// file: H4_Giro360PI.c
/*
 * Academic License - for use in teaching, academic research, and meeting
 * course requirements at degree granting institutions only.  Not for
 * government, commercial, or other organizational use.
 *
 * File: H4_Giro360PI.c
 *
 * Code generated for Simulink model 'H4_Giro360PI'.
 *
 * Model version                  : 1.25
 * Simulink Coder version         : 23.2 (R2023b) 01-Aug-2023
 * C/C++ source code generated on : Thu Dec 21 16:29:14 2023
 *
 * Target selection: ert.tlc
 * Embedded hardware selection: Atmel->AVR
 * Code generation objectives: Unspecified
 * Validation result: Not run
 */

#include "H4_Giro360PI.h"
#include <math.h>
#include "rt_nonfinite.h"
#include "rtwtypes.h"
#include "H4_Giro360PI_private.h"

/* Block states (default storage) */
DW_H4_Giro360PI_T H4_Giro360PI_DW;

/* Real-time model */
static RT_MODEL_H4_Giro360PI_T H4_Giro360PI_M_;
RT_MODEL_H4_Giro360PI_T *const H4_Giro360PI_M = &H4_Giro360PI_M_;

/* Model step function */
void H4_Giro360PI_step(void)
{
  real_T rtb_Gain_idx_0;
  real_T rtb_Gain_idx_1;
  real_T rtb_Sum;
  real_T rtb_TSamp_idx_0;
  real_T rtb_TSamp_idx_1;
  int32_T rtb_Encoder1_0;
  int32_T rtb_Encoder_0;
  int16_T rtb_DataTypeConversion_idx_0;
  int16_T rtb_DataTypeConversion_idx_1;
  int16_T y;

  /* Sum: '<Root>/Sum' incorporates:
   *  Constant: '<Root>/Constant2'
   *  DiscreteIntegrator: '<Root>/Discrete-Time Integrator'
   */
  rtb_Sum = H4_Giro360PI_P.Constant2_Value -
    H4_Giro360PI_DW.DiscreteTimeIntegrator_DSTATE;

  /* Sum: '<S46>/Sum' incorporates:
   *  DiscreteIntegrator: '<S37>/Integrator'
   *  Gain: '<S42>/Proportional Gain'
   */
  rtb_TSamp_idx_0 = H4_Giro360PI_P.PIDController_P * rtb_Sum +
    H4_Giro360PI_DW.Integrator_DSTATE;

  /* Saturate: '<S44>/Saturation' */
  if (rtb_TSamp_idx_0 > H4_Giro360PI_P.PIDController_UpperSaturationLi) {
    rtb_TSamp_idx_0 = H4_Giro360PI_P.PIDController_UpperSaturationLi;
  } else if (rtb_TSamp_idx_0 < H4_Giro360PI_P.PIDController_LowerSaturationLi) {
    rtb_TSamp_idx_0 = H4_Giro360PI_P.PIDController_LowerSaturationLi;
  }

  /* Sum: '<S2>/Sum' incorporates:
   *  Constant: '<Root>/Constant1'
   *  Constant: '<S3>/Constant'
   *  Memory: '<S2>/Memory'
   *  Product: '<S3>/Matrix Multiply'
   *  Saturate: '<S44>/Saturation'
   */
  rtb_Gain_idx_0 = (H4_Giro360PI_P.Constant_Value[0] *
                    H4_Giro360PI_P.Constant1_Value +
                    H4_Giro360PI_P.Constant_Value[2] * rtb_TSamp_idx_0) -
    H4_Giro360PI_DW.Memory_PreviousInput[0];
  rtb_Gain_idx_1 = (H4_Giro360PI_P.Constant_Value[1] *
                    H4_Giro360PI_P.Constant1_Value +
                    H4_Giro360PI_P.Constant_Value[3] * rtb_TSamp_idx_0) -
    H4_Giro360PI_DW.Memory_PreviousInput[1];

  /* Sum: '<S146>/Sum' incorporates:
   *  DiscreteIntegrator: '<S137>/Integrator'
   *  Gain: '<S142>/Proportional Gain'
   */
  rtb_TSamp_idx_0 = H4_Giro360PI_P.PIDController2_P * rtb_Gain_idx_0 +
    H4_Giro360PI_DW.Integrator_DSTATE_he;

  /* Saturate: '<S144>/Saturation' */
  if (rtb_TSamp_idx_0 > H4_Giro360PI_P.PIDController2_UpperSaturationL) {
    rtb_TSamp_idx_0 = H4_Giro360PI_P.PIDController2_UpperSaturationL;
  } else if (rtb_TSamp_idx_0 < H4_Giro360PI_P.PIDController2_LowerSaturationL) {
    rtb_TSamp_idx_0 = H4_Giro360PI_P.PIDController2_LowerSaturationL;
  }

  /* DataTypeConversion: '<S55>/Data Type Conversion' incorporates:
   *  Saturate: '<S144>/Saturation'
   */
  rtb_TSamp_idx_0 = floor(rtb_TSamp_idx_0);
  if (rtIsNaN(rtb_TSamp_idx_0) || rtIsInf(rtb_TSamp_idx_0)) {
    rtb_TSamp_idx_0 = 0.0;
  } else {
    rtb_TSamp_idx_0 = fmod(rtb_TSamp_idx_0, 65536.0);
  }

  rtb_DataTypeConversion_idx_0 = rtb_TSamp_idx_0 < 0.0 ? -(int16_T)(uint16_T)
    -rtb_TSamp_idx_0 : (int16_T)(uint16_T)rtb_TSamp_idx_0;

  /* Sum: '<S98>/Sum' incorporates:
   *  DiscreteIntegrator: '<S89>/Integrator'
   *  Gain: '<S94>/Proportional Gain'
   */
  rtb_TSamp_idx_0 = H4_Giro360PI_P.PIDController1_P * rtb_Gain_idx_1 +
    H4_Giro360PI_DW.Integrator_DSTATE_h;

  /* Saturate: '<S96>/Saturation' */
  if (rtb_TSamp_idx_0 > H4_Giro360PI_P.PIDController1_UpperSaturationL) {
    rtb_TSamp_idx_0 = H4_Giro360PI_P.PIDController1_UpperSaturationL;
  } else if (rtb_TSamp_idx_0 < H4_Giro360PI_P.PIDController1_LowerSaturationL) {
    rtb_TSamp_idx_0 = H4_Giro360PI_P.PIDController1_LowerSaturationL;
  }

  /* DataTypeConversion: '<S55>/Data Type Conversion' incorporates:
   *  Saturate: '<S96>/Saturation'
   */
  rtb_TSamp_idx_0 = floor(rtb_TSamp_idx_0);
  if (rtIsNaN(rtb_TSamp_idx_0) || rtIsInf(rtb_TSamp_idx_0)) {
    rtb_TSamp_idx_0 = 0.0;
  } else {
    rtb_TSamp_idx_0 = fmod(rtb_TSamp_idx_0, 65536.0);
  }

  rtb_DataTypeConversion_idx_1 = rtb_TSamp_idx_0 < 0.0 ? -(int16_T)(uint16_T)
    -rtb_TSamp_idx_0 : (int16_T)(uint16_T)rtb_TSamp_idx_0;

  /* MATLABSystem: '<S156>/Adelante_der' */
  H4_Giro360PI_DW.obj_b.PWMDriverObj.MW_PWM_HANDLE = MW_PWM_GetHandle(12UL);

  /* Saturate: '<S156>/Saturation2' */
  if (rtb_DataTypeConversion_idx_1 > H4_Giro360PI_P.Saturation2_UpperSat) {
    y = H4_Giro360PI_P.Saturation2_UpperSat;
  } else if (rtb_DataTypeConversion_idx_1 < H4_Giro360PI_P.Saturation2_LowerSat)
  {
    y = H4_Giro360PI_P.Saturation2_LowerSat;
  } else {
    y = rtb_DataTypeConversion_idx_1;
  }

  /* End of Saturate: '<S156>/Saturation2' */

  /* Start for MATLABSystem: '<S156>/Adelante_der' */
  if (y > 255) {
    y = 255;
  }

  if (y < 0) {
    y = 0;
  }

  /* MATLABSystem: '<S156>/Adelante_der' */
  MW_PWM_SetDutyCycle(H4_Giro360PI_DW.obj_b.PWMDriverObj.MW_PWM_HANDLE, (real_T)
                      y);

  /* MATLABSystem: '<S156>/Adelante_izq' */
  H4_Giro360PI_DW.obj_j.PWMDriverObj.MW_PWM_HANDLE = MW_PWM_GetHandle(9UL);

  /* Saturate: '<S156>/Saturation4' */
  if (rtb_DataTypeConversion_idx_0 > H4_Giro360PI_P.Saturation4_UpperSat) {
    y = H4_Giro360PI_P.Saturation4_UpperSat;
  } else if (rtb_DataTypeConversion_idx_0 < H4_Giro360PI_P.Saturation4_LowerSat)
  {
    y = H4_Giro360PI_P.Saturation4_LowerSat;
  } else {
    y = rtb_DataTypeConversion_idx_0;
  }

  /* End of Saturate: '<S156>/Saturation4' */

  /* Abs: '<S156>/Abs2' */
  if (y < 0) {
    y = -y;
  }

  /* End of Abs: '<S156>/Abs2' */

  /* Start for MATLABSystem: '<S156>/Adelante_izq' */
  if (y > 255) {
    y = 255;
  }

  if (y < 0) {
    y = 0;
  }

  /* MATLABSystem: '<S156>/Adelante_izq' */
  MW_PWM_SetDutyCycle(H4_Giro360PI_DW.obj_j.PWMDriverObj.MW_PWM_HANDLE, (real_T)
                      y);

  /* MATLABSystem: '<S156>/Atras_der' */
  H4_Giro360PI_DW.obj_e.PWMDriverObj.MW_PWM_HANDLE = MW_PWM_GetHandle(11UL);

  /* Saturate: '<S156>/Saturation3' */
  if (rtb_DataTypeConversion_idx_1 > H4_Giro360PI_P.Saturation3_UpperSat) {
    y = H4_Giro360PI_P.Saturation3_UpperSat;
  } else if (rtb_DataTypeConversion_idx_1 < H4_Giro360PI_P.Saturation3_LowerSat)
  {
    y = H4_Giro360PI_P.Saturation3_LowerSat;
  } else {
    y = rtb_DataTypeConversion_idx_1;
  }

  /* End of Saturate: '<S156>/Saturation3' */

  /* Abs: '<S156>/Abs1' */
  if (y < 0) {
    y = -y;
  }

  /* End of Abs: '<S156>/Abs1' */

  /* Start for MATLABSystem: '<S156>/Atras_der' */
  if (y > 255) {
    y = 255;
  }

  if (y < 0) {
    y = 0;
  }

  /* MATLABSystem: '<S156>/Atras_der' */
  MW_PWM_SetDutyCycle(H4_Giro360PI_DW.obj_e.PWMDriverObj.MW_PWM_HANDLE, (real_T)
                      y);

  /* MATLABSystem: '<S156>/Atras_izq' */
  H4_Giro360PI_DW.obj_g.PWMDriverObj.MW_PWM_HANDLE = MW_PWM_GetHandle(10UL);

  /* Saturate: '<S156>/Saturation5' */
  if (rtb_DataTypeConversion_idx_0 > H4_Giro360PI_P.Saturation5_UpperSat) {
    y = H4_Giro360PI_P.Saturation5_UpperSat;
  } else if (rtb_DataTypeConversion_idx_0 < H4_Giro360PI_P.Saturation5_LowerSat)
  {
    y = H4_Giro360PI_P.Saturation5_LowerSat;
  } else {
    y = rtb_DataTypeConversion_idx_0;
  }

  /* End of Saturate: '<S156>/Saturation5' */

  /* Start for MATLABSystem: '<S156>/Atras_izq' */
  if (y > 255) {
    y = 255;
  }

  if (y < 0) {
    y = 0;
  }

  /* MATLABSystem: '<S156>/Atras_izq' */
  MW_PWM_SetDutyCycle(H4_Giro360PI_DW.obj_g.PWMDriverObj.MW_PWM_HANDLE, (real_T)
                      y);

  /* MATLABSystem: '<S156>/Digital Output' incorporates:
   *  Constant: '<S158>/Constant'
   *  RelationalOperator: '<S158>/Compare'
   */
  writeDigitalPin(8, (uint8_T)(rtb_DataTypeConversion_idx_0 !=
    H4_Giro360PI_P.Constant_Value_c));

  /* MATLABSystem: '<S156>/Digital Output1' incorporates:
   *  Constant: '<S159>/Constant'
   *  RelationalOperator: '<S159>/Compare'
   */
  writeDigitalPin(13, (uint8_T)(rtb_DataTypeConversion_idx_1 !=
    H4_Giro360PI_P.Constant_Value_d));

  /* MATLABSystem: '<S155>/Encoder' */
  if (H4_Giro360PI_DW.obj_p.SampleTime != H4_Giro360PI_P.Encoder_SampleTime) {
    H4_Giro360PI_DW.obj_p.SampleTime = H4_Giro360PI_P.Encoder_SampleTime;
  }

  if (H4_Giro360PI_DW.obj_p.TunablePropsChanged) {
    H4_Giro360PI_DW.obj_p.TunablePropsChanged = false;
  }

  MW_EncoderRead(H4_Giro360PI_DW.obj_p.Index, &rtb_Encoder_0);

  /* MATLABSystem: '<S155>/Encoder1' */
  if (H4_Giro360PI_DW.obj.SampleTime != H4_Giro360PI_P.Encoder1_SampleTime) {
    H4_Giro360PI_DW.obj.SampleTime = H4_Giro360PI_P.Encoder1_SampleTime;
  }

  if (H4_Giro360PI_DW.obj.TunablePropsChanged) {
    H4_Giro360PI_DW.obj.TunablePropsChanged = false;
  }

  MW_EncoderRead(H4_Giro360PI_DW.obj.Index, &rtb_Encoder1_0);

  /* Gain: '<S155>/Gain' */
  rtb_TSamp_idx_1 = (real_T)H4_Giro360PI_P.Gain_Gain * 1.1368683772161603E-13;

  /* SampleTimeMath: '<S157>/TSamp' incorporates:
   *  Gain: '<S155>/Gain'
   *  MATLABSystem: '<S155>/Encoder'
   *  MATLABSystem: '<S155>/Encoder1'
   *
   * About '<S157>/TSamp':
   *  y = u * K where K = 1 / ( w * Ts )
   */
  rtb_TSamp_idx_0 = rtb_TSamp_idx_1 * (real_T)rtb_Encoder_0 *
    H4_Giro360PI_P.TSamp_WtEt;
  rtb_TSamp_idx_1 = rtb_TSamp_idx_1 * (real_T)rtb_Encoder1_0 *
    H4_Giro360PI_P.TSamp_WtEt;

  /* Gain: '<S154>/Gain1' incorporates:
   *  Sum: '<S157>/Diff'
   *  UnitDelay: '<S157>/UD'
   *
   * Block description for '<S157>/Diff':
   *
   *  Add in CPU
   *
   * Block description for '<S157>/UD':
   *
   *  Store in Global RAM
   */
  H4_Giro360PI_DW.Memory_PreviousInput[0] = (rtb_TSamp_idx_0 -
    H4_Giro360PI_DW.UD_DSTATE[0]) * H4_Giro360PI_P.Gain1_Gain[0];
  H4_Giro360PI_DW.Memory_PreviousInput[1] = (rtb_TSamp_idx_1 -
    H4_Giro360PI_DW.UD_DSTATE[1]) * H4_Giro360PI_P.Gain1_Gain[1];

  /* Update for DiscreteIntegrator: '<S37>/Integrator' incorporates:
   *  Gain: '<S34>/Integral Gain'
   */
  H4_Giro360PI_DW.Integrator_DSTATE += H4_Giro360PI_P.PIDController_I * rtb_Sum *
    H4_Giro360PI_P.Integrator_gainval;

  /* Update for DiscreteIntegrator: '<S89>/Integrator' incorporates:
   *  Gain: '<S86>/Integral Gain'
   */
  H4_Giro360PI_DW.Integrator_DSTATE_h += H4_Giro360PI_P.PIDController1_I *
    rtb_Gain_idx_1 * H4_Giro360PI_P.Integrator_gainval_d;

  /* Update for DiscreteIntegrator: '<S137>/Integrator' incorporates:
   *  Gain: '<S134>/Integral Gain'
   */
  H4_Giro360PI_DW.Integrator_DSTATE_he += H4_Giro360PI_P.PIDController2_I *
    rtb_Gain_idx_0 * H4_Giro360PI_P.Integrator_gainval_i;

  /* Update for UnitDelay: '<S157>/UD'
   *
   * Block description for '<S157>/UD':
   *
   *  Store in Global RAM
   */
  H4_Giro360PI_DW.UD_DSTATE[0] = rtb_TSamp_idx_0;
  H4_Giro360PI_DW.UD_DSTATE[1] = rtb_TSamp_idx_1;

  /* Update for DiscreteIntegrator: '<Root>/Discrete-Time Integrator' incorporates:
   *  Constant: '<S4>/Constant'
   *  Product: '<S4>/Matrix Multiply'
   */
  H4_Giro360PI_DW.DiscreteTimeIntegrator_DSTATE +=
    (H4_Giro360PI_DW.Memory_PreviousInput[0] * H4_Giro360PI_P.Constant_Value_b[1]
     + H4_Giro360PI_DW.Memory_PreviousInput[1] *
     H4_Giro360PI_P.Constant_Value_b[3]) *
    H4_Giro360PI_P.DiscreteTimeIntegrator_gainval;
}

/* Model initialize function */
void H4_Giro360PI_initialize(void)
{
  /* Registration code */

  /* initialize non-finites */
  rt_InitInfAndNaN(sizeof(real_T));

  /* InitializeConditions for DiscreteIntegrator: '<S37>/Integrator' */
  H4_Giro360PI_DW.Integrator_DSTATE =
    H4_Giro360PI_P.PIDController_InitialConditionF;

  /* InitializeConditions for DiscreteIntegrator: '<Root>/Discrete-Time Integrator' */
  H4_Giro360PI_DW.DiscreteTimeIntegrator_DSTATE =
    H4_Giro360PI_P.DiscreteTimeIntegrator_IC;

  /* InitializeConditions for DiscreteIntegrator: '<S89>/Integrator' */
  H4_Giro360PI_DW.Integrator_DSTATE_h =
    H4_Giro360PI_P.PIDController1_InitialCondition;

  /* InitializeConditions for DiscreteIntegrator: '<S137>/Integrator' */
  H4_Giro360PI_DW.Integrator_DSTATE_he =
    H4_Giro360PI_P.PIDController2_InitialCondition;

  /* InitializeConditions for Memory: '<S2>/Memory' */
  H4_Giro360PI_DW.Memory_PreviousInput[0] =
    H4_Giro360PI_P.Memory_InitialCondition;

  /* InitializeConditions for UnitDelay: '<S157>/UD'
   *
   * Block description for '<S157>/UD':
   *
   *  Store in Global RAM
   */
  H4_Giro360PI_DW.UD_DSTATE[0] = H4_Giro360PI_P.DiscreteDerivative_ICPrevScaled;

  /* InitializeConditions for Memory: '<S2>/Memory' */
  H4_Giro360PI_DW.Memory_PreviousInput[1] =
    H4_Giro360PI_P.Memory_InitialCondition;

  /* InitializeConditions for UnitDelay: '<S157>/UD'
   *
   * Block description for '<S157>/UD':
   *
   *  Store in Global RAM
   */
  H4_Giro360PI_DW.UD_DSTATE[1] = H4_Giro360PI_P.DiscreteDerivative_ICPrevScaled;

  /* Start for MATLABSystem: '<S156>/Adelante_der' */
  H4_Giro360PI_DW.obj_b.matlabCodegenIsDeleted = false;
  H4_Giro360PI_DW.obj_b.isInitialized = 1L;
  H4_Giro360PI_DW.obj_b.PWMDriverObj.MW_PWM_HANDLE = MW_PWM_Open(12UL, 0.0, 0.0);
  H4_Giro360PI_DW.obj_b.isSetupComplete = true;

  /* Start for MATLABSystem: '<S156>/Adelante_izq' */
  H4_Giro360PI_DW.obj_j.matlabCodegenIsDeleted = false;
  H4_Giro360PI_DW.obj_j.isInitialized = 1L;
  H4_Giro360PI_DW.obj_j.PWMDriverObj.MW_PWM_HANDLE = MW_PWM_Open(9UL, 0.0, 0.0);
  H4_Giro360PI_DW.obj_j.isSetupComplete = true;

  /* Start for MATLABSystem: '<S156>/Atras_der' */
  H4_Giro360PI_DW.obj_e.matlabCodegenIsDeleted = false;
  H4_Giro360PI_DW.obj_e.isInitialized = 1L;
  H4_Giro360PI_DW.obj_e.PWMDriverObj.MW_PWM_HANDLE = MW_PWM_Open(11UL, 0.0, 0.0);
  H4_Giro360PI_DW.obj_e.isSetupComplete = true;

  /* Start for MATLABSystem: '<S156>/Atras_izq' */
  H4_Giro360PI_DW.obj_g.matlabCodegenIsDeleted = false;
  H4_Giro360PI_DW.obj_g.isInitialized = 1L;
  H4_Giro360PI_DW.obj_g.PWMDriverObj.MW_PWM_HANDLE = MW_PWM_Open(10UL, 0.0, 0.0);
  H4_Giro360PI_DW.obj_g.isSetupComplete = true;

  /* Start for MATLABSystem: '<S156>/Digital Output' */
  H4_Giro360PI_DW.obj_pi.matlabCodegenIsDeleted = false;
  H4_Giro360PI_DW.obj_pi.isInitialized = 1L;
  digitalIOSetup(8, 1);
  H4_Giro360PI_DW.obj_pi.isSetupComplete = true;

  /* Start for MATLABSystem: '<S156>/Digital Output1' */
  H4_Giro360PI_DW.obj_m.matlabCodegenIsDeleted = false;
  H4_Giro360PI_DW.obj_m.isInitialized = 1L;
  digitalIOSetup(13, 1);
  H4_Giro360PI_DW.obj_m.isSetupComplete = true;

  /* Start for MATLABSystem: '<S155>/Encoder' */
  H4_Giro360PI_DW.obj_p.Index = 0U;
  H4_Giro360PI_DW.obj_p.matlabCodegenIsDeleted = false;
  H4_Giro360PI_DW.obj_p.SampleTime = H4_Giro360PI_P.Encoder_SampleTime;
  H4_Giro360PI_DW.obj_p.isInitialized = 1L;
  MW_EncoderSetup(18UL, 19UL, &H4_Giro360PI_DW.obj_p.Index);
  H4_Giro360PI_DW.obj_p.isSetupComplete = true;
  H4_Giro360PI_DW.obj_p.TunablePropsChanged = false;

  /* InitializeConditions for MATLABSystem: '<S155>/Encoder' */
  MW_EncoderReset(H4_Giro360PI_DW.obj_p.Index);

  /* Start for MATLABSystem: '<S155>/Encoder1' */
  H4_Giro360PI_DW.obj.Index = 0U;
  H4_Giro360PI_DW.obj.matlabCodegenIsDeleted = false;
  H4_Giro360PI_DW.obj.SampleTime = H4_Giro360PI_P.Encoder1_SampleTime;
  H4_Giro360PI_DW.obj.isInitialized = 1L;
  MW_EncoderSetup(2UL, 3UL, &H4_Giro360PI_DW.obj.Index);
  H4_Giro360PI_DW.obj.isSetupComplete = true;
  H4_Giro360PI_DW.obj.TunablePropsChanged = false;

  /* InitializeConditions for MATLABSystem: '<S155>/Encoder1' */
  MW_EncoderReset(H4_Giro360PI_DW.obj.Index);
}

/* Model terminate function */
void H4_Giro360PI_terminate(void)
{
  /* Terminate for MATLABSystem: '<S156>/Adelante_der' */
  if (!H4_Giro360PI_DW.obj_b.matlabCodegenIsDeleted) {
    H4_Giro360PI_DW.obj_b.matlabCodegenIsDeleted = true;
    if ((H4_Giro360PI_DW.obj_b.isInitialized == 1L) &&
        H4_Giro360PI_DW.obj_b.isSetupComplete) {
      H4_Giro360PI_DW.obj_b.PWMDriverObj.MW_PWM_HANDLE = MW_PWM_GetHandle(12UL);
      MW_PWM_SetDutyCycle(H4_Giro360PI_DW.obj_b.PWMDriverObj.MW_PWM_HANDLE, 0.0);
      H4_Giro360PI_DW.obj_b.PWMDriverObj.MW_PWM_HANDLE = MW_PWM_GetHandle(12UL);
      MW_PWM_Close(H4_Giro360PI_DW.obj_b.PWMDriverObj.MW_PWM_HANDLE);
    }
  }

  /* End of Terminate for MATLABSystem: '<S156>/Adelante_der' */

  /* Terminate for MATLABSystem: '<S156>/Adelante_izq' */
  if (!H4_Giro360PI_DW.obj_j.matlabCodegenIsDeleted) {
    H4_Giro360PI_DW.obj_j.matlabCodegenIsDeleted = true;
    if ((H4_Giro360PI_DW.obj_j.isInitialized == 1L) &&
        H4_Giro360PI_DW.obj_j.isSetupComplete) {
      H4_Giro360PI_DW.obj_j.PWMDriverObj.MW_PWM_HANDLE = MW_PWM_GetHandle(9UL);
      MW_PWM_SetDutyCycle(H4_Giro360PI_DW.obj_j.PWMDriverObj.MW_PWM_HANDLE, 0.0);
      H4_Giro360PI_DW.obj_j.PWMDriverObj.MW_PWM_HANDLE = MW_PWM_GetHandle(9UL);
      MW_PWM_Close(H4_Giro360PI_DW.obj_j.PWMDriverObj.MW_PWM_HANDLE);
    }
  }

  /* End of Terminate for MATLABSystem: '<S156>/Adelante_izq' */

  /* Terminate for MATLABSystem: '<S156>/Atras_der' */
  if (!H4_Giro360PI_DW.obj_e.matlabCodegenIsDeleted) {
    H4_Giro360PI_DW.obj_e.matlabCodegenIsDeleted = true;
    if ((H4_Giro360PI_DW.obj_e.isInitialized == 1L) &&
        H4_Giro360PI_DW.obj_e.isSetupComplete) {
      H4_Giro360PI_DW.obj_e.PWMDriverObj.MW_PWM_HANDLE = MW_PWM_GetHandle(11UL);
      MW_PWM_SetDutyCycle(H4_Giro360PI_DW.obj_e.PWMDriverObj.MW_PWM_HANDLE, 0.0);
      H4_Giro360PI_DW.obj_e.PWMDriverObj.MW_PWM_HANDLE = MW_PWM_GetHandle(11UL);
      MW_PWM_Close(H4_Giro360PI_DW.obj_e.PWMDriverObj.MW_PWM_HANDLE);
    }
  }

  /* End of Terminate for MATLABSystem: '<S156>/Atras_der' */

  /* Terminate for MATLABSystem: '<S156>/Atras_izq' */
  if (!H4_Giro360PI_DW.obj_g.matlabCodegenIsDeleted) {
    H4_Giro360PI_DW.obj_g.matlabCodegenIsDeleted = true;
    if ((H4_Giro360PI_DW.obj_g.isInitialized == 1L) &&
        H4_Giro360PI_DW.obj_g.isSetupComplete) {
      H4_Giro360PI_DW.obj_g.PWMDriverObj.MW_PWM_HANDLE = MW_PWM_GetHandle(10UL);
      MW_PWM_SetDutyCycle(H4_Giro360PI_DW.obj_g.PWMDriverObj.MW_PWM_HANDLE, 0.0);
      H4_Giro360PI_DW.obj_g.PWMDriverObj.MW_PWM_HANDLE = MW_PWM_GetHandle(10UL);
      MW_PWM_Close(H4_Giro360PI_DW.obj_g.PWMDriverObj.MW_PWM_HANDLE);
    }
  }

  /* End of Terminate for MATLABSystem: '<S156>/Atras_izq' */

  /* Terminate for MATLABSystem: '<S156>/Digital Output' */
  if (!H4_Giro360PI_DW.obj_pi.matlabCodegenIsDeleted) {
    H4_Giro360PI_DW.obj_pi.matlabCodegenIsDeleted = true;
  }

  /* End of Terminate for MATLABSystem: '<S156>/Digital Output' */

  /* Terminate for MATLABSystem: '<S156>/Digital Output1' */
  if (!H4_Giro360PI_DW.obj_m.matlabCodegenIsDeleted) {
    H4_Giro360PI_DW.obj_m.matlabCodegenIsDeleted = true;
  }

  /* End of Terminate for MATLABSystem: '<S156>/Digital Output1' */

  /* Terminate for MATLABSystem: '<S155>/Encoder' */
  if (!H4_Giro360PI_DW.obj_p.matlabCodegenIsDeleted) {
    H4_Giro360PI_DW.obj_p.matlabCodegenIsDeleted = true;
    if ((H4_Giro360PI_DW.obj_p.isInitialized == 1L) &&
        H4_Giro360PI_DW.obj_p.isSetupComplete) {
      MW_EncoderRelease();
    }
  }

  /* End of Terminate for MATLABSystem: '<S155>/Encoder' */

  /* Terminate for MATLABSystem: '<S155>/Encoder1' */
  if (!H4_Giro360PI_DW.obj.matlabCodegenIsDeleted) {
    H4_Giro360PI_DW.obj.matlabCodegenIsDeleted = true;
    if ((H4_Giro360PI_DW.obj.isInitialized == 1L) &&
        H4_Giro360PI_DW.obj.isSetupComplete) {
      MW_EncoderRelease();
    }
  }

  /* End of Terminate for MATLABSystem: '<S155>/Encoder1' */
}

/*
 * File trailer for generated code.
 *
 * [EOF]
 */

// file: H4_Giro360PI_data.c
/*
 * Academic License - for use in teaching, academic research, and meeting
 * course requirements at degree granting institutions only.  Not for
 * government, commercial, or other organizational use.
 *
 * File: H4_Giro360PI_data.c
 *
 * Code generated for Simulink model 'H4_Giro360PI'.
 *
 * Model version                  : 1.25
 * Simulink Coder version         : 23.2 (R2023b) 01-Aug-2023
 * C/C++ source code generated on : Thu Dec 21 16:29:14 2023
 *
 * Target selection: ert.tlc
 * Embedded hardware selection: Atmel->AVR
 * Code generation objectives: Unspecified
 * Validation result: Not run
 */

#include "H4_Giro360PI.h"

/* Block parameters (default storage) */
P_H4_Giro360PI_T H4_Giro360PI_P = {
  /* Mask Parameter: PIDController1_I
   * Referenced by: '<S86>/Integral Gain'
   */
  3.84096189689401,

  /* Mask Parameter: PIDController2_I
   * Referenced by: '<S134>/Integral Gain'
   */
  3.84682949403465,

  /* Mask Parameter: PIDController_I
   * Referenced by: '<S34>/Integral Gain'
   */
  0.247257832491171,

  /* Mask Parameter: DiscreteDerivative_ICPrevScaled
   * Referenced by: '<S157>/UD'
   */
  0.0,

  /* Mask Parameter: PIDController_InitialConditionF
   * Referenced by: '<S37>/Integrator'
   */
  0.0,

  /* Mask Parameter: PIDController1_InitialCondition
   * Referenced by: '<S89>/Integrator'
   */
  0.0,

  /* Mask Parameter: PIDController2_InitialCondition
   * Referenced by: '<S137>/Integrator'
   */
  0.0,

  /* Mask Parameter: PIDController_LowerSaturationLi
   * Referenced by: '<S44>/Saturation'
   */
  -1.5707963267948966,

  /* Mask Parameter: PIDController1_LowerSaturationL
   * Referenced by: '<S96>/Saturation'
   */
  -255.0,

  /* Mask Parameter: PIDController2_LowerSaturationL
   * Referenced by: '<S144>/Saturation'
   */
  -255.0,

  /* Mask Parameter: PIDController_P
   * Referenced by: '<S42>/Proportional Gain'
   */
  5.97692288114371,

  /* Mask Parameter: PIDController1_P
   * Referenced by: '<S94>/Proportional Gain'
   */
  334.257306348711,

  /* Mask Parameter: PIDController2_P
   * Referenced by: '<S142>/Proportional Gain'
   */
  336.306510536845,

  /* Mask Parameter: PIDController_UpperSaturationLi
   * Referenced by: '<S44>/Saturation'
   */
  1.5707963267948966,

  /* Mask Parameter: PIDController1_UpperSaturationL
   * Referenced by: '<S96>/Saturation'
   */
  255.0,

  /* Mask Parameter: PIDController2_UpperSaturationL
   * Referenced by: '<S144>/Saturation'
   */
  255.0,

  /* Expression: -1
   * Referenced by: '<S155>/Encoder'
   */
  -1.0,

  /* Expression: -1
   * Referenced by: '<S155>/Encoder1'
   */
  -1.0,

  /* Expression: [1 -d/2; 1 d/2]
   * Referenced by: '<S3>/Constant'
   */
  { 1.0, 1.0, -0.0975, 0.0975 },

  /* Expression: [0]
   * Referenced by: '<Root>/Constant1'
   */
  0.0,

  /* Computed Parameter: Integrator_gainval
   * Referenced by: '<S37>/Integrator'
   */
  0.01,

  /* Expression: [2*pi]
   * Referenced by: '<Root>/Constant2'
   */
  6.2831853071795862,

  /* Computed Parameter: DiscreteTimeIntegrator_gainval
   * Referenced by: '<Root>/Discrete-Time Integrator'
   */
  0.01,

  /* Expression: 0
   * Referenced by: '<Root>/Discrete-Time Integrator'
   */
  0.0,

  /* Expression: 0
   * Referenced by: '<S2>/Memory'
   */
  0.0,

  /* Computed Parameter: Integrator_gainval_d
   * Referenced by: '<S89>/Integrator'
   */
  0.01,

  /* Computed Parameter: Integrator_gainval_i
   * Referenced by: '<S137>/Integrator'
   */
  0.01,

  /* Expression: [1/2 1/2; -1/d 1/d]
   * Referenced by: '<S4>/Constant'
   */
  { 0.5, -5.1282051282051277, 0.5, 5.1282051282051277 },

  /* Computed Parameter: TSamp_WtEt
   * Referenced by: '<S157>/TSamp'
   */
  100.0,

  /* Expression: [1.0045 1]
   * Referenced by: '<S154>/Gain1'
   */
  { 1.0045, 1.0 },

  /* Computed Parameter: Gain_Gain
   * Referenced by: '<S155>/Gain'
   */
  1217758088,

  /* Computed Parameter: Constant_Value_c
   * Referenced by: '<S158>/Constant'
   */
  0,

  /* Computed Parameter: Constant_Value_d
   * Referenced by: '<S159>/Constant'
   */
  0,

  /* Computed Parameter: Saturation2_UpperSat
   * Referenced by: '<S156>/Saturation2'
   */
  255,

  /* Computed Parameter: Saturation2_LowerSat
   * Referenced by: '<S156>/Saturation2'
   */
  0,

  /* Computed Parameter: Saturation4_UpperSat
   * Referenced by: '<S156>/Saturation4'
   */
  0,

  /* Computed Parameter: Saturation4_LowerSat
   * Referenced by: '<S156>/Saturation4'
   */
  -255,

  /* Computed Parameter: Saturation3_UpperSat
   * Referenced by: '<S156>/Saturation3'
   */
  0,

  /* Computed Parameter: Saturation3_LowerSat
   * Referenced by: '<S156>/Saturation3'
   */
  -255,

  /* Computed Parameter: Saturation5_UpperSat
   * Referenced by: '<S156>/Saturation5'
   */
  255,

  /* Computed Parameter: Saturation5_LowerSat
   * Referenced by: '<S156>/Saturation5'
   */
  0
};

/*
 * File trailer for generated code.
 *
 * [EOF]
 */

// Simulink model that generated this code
simulink model "H4_Giro360PI"  (R2023b)
settings: Solver=FixedStepDiscrete  StartTime=0.0  StopTime=10  FixedStep=0.01  RelTol=1e-3  EnableMultiTasking=on
model workspace (MAT data in the model file):
  d = 0.195
undefined symbols (not defined in the file or in its folder): DiscIntNeverNeededParam
libraries: slpidlib x1

== system H4_Giro360PI ==
  Constant1 : Constant  Value=[0]
  Constant2 : Constant  Value=[2*pi]
  Demux : Demux  Outputs=2
  Discrete-Time Integrator : DiscreteIntegrator  SampleTime=-1  ICPrevOutput=DiscIntNeverNeededParam  ICPrevScaledInput=DiscIntNeverNeededParam
  Mux : Mux  Inputs=2
  PID Controller : slpidlib/PID Controller  Controller=PI  Form=Parallel  TimeDomain=Discrete-time  UseExternalTs=off  SampleTime=-1  IntegratorMethod=Forward Euler  FilterMethod=Forward Euler  ControllerParametersSource=internal  P=5.97692288114371  I=0.247257832491171  UseKiTs=off  D=0  N=100  UseFilter=on  TunerSelectOption=Transfer Function Based (PID Tuner App)  InitialConditionSource=internal  InitialConditionForIntegrator=0  InitialConditionForFilter=0  DifferentiatorICPrevScaledInput=0  ExternalReset=none  TrackingMode=off  Kt=1  LimitOutput=on  SatLimitsSource=internal  UpperSaturationLimit=2*pi/4  LowerSaturationLimit=-2*pi/4  LinearizeAsGain=off  AntiWindupMode=none  Kb=1  LimitIntegrator=off  UpperIntegratorSaturationLimit=inf  LowerIntegratorSaturationLimit=-inf  POutMin=[]  POutMax=[]  IOutMin=[]  IOutMax=[]  DOutMin=[]  DOutMax=[]  NOutMin=[]  NOutMax=[]  SumOutMin=[]  SumOutMax=[]  SaturationOutMin=[]  SaturationOutMax=[]  PParamMin=[]  PParamMax=[]  IParamMin=[]  IParamMax=[]  DParamMin=[]  DParamMax=[]  NParamMin=[]  NParamMax=[]  KbParamMin=[]  KbParamMax=[]  KtParamMin=[]  KtParamMax=[]  KbOutMin=[]  KbOutMax=[]  KtOutMin=[]  KtOutMax=[]  IntegratorOutMin=[]  IntegratorOutMax=[]  FilterOutMin=[]  FilterOutMax=[]  SumI1OutMin=[]  SumI1OutMax=[]  SumI2OutMin=[]  SumI2OutMax=[]  SumI3OutMin=[]  SumI3OutMax=[]  SumI4OutMin=[]  SumI4OutMax=[]  SumDOutMin=[]  SumDOutMax=[]  DifferentiatorOutMin=[]  DifferentiatorOutMax=[]  FilterDiffOutCoefMin=[]  FilterDiffOutCoefMax=[]  ReciprocalOutMin=[]  ReciprocalOutMax=[]  SumDenOutMin=[]  SumDenOutMax=[]  SumNumOutMin=[]  SumNumOutMax=[]  DivideOutMin=[]  DivideOutMax=[]  UdiffTsProdOutMin=[]  UdiffTsProdOutMax=[]  NTsProdOutMin=[]  NTsProdOutMax=[]  UintegralTsProdOutMin=[]  UintegralTsProdOutMax=[]  UngainTsProdOutMin=[]  UngainTsProdOutMax=[]  ClampingZeroOutDataTypeStr=Inherit: Inherit via back propagation  ClampingZeroOutMin=[]  ClampingZeroOutMax=[]  FilterDenConstantOutDataTypeStr=Inherit: Inherit via back propagation  FilterDenConstantOutMin=[]  FilterDenConstantOutMax=[]  PCopyOutDataTypeStr=Inherit: Inherit via back propagation  PCopyOutMin=[]  PCopyOutMax=[]  NCopyOutDataTypeStr=Inherit: Inherit via back propagation  NCopyOutMin=[]  NCopyOutMax=[]  IntegratorContinuousStateAttributes=''  IntegratorStateMustResolveToSignalObject=off  IntegratorRTWStateStorageClass=Auto  FilterContinuousStateAttributes=''  FilterStateMustResolveToSignalObject=off  FilterRTWStateStorageClass=Auto  ParallelPVariant=InternalParameters  IdealPVariant=Disabled  IVariant=InternalParameters  DVariant=Disabled  IntegratorVariant=Discrete  SatVariant=Enabled  AWVariant=Passthrough  PCopyVariant=Disabled  TRVariant=Disabled  FdbkBlocksVariant=Forward  IdealPFdbkVariant=Disabled  SatFdbkVariant=Disabled  DerivativeFilterVariant=Disabled  NVariant=Disabled  NCopyVariant=Disabled_SignalSpec  FilterICVariant=Disabled  IntegratorICVariant=InternalICs  ExternalResetVariant=Disabled  TRSumVariant=Passthrough  SumFdbkVariant=Disabled  SumVariant=Sum_PI  TsampFilterVariant=InternalTs  TsampNgainVariant=Passthrough  TsampIntegralVariant=Disabled_SignalSpec  ExternalSaturationOutDataTypeStr=Inherit: Same as second input
  Subsystem Reference : Subsystem  ReferencedSubsystem=Piero_ControladoZ_memoria
  Subsystem Reference1 : Subsystem  ReferencedSubsystem=MCI2
  Subsystem Reference2 : Subsystem  ReferencedSubsystem=MCD2
  Subsystem Reference4 : Subsystem  ReferencedSubsystem=OdometriaZ
  Sum : Sum  Inputs=|+-
  Terminator : Terminator
  wires:
  Subsystem Reference1/1 -> Subsystem Reference/1
  Subsystem Reference2/1 -> Demux/1, Subsystem Reference4/1
  Subsystem Reference/1 -> Subsystem Reference2/1
  PID Controller/1 -> Mux/2  "rel"
  Mux/1 -> Subsystem Reference1/1  "Linea1"
  Constant1/1 -> Mux/1
  Sum/1 -> PID Controller/1
  Constant2/1 -> Sum/1
  Demux/1 -> Terminator/1
  Demux/2 -> Discrete-Time Integrator/1
  Discrete-Time Integrator/1 -> Sum/2  "Linea2"
